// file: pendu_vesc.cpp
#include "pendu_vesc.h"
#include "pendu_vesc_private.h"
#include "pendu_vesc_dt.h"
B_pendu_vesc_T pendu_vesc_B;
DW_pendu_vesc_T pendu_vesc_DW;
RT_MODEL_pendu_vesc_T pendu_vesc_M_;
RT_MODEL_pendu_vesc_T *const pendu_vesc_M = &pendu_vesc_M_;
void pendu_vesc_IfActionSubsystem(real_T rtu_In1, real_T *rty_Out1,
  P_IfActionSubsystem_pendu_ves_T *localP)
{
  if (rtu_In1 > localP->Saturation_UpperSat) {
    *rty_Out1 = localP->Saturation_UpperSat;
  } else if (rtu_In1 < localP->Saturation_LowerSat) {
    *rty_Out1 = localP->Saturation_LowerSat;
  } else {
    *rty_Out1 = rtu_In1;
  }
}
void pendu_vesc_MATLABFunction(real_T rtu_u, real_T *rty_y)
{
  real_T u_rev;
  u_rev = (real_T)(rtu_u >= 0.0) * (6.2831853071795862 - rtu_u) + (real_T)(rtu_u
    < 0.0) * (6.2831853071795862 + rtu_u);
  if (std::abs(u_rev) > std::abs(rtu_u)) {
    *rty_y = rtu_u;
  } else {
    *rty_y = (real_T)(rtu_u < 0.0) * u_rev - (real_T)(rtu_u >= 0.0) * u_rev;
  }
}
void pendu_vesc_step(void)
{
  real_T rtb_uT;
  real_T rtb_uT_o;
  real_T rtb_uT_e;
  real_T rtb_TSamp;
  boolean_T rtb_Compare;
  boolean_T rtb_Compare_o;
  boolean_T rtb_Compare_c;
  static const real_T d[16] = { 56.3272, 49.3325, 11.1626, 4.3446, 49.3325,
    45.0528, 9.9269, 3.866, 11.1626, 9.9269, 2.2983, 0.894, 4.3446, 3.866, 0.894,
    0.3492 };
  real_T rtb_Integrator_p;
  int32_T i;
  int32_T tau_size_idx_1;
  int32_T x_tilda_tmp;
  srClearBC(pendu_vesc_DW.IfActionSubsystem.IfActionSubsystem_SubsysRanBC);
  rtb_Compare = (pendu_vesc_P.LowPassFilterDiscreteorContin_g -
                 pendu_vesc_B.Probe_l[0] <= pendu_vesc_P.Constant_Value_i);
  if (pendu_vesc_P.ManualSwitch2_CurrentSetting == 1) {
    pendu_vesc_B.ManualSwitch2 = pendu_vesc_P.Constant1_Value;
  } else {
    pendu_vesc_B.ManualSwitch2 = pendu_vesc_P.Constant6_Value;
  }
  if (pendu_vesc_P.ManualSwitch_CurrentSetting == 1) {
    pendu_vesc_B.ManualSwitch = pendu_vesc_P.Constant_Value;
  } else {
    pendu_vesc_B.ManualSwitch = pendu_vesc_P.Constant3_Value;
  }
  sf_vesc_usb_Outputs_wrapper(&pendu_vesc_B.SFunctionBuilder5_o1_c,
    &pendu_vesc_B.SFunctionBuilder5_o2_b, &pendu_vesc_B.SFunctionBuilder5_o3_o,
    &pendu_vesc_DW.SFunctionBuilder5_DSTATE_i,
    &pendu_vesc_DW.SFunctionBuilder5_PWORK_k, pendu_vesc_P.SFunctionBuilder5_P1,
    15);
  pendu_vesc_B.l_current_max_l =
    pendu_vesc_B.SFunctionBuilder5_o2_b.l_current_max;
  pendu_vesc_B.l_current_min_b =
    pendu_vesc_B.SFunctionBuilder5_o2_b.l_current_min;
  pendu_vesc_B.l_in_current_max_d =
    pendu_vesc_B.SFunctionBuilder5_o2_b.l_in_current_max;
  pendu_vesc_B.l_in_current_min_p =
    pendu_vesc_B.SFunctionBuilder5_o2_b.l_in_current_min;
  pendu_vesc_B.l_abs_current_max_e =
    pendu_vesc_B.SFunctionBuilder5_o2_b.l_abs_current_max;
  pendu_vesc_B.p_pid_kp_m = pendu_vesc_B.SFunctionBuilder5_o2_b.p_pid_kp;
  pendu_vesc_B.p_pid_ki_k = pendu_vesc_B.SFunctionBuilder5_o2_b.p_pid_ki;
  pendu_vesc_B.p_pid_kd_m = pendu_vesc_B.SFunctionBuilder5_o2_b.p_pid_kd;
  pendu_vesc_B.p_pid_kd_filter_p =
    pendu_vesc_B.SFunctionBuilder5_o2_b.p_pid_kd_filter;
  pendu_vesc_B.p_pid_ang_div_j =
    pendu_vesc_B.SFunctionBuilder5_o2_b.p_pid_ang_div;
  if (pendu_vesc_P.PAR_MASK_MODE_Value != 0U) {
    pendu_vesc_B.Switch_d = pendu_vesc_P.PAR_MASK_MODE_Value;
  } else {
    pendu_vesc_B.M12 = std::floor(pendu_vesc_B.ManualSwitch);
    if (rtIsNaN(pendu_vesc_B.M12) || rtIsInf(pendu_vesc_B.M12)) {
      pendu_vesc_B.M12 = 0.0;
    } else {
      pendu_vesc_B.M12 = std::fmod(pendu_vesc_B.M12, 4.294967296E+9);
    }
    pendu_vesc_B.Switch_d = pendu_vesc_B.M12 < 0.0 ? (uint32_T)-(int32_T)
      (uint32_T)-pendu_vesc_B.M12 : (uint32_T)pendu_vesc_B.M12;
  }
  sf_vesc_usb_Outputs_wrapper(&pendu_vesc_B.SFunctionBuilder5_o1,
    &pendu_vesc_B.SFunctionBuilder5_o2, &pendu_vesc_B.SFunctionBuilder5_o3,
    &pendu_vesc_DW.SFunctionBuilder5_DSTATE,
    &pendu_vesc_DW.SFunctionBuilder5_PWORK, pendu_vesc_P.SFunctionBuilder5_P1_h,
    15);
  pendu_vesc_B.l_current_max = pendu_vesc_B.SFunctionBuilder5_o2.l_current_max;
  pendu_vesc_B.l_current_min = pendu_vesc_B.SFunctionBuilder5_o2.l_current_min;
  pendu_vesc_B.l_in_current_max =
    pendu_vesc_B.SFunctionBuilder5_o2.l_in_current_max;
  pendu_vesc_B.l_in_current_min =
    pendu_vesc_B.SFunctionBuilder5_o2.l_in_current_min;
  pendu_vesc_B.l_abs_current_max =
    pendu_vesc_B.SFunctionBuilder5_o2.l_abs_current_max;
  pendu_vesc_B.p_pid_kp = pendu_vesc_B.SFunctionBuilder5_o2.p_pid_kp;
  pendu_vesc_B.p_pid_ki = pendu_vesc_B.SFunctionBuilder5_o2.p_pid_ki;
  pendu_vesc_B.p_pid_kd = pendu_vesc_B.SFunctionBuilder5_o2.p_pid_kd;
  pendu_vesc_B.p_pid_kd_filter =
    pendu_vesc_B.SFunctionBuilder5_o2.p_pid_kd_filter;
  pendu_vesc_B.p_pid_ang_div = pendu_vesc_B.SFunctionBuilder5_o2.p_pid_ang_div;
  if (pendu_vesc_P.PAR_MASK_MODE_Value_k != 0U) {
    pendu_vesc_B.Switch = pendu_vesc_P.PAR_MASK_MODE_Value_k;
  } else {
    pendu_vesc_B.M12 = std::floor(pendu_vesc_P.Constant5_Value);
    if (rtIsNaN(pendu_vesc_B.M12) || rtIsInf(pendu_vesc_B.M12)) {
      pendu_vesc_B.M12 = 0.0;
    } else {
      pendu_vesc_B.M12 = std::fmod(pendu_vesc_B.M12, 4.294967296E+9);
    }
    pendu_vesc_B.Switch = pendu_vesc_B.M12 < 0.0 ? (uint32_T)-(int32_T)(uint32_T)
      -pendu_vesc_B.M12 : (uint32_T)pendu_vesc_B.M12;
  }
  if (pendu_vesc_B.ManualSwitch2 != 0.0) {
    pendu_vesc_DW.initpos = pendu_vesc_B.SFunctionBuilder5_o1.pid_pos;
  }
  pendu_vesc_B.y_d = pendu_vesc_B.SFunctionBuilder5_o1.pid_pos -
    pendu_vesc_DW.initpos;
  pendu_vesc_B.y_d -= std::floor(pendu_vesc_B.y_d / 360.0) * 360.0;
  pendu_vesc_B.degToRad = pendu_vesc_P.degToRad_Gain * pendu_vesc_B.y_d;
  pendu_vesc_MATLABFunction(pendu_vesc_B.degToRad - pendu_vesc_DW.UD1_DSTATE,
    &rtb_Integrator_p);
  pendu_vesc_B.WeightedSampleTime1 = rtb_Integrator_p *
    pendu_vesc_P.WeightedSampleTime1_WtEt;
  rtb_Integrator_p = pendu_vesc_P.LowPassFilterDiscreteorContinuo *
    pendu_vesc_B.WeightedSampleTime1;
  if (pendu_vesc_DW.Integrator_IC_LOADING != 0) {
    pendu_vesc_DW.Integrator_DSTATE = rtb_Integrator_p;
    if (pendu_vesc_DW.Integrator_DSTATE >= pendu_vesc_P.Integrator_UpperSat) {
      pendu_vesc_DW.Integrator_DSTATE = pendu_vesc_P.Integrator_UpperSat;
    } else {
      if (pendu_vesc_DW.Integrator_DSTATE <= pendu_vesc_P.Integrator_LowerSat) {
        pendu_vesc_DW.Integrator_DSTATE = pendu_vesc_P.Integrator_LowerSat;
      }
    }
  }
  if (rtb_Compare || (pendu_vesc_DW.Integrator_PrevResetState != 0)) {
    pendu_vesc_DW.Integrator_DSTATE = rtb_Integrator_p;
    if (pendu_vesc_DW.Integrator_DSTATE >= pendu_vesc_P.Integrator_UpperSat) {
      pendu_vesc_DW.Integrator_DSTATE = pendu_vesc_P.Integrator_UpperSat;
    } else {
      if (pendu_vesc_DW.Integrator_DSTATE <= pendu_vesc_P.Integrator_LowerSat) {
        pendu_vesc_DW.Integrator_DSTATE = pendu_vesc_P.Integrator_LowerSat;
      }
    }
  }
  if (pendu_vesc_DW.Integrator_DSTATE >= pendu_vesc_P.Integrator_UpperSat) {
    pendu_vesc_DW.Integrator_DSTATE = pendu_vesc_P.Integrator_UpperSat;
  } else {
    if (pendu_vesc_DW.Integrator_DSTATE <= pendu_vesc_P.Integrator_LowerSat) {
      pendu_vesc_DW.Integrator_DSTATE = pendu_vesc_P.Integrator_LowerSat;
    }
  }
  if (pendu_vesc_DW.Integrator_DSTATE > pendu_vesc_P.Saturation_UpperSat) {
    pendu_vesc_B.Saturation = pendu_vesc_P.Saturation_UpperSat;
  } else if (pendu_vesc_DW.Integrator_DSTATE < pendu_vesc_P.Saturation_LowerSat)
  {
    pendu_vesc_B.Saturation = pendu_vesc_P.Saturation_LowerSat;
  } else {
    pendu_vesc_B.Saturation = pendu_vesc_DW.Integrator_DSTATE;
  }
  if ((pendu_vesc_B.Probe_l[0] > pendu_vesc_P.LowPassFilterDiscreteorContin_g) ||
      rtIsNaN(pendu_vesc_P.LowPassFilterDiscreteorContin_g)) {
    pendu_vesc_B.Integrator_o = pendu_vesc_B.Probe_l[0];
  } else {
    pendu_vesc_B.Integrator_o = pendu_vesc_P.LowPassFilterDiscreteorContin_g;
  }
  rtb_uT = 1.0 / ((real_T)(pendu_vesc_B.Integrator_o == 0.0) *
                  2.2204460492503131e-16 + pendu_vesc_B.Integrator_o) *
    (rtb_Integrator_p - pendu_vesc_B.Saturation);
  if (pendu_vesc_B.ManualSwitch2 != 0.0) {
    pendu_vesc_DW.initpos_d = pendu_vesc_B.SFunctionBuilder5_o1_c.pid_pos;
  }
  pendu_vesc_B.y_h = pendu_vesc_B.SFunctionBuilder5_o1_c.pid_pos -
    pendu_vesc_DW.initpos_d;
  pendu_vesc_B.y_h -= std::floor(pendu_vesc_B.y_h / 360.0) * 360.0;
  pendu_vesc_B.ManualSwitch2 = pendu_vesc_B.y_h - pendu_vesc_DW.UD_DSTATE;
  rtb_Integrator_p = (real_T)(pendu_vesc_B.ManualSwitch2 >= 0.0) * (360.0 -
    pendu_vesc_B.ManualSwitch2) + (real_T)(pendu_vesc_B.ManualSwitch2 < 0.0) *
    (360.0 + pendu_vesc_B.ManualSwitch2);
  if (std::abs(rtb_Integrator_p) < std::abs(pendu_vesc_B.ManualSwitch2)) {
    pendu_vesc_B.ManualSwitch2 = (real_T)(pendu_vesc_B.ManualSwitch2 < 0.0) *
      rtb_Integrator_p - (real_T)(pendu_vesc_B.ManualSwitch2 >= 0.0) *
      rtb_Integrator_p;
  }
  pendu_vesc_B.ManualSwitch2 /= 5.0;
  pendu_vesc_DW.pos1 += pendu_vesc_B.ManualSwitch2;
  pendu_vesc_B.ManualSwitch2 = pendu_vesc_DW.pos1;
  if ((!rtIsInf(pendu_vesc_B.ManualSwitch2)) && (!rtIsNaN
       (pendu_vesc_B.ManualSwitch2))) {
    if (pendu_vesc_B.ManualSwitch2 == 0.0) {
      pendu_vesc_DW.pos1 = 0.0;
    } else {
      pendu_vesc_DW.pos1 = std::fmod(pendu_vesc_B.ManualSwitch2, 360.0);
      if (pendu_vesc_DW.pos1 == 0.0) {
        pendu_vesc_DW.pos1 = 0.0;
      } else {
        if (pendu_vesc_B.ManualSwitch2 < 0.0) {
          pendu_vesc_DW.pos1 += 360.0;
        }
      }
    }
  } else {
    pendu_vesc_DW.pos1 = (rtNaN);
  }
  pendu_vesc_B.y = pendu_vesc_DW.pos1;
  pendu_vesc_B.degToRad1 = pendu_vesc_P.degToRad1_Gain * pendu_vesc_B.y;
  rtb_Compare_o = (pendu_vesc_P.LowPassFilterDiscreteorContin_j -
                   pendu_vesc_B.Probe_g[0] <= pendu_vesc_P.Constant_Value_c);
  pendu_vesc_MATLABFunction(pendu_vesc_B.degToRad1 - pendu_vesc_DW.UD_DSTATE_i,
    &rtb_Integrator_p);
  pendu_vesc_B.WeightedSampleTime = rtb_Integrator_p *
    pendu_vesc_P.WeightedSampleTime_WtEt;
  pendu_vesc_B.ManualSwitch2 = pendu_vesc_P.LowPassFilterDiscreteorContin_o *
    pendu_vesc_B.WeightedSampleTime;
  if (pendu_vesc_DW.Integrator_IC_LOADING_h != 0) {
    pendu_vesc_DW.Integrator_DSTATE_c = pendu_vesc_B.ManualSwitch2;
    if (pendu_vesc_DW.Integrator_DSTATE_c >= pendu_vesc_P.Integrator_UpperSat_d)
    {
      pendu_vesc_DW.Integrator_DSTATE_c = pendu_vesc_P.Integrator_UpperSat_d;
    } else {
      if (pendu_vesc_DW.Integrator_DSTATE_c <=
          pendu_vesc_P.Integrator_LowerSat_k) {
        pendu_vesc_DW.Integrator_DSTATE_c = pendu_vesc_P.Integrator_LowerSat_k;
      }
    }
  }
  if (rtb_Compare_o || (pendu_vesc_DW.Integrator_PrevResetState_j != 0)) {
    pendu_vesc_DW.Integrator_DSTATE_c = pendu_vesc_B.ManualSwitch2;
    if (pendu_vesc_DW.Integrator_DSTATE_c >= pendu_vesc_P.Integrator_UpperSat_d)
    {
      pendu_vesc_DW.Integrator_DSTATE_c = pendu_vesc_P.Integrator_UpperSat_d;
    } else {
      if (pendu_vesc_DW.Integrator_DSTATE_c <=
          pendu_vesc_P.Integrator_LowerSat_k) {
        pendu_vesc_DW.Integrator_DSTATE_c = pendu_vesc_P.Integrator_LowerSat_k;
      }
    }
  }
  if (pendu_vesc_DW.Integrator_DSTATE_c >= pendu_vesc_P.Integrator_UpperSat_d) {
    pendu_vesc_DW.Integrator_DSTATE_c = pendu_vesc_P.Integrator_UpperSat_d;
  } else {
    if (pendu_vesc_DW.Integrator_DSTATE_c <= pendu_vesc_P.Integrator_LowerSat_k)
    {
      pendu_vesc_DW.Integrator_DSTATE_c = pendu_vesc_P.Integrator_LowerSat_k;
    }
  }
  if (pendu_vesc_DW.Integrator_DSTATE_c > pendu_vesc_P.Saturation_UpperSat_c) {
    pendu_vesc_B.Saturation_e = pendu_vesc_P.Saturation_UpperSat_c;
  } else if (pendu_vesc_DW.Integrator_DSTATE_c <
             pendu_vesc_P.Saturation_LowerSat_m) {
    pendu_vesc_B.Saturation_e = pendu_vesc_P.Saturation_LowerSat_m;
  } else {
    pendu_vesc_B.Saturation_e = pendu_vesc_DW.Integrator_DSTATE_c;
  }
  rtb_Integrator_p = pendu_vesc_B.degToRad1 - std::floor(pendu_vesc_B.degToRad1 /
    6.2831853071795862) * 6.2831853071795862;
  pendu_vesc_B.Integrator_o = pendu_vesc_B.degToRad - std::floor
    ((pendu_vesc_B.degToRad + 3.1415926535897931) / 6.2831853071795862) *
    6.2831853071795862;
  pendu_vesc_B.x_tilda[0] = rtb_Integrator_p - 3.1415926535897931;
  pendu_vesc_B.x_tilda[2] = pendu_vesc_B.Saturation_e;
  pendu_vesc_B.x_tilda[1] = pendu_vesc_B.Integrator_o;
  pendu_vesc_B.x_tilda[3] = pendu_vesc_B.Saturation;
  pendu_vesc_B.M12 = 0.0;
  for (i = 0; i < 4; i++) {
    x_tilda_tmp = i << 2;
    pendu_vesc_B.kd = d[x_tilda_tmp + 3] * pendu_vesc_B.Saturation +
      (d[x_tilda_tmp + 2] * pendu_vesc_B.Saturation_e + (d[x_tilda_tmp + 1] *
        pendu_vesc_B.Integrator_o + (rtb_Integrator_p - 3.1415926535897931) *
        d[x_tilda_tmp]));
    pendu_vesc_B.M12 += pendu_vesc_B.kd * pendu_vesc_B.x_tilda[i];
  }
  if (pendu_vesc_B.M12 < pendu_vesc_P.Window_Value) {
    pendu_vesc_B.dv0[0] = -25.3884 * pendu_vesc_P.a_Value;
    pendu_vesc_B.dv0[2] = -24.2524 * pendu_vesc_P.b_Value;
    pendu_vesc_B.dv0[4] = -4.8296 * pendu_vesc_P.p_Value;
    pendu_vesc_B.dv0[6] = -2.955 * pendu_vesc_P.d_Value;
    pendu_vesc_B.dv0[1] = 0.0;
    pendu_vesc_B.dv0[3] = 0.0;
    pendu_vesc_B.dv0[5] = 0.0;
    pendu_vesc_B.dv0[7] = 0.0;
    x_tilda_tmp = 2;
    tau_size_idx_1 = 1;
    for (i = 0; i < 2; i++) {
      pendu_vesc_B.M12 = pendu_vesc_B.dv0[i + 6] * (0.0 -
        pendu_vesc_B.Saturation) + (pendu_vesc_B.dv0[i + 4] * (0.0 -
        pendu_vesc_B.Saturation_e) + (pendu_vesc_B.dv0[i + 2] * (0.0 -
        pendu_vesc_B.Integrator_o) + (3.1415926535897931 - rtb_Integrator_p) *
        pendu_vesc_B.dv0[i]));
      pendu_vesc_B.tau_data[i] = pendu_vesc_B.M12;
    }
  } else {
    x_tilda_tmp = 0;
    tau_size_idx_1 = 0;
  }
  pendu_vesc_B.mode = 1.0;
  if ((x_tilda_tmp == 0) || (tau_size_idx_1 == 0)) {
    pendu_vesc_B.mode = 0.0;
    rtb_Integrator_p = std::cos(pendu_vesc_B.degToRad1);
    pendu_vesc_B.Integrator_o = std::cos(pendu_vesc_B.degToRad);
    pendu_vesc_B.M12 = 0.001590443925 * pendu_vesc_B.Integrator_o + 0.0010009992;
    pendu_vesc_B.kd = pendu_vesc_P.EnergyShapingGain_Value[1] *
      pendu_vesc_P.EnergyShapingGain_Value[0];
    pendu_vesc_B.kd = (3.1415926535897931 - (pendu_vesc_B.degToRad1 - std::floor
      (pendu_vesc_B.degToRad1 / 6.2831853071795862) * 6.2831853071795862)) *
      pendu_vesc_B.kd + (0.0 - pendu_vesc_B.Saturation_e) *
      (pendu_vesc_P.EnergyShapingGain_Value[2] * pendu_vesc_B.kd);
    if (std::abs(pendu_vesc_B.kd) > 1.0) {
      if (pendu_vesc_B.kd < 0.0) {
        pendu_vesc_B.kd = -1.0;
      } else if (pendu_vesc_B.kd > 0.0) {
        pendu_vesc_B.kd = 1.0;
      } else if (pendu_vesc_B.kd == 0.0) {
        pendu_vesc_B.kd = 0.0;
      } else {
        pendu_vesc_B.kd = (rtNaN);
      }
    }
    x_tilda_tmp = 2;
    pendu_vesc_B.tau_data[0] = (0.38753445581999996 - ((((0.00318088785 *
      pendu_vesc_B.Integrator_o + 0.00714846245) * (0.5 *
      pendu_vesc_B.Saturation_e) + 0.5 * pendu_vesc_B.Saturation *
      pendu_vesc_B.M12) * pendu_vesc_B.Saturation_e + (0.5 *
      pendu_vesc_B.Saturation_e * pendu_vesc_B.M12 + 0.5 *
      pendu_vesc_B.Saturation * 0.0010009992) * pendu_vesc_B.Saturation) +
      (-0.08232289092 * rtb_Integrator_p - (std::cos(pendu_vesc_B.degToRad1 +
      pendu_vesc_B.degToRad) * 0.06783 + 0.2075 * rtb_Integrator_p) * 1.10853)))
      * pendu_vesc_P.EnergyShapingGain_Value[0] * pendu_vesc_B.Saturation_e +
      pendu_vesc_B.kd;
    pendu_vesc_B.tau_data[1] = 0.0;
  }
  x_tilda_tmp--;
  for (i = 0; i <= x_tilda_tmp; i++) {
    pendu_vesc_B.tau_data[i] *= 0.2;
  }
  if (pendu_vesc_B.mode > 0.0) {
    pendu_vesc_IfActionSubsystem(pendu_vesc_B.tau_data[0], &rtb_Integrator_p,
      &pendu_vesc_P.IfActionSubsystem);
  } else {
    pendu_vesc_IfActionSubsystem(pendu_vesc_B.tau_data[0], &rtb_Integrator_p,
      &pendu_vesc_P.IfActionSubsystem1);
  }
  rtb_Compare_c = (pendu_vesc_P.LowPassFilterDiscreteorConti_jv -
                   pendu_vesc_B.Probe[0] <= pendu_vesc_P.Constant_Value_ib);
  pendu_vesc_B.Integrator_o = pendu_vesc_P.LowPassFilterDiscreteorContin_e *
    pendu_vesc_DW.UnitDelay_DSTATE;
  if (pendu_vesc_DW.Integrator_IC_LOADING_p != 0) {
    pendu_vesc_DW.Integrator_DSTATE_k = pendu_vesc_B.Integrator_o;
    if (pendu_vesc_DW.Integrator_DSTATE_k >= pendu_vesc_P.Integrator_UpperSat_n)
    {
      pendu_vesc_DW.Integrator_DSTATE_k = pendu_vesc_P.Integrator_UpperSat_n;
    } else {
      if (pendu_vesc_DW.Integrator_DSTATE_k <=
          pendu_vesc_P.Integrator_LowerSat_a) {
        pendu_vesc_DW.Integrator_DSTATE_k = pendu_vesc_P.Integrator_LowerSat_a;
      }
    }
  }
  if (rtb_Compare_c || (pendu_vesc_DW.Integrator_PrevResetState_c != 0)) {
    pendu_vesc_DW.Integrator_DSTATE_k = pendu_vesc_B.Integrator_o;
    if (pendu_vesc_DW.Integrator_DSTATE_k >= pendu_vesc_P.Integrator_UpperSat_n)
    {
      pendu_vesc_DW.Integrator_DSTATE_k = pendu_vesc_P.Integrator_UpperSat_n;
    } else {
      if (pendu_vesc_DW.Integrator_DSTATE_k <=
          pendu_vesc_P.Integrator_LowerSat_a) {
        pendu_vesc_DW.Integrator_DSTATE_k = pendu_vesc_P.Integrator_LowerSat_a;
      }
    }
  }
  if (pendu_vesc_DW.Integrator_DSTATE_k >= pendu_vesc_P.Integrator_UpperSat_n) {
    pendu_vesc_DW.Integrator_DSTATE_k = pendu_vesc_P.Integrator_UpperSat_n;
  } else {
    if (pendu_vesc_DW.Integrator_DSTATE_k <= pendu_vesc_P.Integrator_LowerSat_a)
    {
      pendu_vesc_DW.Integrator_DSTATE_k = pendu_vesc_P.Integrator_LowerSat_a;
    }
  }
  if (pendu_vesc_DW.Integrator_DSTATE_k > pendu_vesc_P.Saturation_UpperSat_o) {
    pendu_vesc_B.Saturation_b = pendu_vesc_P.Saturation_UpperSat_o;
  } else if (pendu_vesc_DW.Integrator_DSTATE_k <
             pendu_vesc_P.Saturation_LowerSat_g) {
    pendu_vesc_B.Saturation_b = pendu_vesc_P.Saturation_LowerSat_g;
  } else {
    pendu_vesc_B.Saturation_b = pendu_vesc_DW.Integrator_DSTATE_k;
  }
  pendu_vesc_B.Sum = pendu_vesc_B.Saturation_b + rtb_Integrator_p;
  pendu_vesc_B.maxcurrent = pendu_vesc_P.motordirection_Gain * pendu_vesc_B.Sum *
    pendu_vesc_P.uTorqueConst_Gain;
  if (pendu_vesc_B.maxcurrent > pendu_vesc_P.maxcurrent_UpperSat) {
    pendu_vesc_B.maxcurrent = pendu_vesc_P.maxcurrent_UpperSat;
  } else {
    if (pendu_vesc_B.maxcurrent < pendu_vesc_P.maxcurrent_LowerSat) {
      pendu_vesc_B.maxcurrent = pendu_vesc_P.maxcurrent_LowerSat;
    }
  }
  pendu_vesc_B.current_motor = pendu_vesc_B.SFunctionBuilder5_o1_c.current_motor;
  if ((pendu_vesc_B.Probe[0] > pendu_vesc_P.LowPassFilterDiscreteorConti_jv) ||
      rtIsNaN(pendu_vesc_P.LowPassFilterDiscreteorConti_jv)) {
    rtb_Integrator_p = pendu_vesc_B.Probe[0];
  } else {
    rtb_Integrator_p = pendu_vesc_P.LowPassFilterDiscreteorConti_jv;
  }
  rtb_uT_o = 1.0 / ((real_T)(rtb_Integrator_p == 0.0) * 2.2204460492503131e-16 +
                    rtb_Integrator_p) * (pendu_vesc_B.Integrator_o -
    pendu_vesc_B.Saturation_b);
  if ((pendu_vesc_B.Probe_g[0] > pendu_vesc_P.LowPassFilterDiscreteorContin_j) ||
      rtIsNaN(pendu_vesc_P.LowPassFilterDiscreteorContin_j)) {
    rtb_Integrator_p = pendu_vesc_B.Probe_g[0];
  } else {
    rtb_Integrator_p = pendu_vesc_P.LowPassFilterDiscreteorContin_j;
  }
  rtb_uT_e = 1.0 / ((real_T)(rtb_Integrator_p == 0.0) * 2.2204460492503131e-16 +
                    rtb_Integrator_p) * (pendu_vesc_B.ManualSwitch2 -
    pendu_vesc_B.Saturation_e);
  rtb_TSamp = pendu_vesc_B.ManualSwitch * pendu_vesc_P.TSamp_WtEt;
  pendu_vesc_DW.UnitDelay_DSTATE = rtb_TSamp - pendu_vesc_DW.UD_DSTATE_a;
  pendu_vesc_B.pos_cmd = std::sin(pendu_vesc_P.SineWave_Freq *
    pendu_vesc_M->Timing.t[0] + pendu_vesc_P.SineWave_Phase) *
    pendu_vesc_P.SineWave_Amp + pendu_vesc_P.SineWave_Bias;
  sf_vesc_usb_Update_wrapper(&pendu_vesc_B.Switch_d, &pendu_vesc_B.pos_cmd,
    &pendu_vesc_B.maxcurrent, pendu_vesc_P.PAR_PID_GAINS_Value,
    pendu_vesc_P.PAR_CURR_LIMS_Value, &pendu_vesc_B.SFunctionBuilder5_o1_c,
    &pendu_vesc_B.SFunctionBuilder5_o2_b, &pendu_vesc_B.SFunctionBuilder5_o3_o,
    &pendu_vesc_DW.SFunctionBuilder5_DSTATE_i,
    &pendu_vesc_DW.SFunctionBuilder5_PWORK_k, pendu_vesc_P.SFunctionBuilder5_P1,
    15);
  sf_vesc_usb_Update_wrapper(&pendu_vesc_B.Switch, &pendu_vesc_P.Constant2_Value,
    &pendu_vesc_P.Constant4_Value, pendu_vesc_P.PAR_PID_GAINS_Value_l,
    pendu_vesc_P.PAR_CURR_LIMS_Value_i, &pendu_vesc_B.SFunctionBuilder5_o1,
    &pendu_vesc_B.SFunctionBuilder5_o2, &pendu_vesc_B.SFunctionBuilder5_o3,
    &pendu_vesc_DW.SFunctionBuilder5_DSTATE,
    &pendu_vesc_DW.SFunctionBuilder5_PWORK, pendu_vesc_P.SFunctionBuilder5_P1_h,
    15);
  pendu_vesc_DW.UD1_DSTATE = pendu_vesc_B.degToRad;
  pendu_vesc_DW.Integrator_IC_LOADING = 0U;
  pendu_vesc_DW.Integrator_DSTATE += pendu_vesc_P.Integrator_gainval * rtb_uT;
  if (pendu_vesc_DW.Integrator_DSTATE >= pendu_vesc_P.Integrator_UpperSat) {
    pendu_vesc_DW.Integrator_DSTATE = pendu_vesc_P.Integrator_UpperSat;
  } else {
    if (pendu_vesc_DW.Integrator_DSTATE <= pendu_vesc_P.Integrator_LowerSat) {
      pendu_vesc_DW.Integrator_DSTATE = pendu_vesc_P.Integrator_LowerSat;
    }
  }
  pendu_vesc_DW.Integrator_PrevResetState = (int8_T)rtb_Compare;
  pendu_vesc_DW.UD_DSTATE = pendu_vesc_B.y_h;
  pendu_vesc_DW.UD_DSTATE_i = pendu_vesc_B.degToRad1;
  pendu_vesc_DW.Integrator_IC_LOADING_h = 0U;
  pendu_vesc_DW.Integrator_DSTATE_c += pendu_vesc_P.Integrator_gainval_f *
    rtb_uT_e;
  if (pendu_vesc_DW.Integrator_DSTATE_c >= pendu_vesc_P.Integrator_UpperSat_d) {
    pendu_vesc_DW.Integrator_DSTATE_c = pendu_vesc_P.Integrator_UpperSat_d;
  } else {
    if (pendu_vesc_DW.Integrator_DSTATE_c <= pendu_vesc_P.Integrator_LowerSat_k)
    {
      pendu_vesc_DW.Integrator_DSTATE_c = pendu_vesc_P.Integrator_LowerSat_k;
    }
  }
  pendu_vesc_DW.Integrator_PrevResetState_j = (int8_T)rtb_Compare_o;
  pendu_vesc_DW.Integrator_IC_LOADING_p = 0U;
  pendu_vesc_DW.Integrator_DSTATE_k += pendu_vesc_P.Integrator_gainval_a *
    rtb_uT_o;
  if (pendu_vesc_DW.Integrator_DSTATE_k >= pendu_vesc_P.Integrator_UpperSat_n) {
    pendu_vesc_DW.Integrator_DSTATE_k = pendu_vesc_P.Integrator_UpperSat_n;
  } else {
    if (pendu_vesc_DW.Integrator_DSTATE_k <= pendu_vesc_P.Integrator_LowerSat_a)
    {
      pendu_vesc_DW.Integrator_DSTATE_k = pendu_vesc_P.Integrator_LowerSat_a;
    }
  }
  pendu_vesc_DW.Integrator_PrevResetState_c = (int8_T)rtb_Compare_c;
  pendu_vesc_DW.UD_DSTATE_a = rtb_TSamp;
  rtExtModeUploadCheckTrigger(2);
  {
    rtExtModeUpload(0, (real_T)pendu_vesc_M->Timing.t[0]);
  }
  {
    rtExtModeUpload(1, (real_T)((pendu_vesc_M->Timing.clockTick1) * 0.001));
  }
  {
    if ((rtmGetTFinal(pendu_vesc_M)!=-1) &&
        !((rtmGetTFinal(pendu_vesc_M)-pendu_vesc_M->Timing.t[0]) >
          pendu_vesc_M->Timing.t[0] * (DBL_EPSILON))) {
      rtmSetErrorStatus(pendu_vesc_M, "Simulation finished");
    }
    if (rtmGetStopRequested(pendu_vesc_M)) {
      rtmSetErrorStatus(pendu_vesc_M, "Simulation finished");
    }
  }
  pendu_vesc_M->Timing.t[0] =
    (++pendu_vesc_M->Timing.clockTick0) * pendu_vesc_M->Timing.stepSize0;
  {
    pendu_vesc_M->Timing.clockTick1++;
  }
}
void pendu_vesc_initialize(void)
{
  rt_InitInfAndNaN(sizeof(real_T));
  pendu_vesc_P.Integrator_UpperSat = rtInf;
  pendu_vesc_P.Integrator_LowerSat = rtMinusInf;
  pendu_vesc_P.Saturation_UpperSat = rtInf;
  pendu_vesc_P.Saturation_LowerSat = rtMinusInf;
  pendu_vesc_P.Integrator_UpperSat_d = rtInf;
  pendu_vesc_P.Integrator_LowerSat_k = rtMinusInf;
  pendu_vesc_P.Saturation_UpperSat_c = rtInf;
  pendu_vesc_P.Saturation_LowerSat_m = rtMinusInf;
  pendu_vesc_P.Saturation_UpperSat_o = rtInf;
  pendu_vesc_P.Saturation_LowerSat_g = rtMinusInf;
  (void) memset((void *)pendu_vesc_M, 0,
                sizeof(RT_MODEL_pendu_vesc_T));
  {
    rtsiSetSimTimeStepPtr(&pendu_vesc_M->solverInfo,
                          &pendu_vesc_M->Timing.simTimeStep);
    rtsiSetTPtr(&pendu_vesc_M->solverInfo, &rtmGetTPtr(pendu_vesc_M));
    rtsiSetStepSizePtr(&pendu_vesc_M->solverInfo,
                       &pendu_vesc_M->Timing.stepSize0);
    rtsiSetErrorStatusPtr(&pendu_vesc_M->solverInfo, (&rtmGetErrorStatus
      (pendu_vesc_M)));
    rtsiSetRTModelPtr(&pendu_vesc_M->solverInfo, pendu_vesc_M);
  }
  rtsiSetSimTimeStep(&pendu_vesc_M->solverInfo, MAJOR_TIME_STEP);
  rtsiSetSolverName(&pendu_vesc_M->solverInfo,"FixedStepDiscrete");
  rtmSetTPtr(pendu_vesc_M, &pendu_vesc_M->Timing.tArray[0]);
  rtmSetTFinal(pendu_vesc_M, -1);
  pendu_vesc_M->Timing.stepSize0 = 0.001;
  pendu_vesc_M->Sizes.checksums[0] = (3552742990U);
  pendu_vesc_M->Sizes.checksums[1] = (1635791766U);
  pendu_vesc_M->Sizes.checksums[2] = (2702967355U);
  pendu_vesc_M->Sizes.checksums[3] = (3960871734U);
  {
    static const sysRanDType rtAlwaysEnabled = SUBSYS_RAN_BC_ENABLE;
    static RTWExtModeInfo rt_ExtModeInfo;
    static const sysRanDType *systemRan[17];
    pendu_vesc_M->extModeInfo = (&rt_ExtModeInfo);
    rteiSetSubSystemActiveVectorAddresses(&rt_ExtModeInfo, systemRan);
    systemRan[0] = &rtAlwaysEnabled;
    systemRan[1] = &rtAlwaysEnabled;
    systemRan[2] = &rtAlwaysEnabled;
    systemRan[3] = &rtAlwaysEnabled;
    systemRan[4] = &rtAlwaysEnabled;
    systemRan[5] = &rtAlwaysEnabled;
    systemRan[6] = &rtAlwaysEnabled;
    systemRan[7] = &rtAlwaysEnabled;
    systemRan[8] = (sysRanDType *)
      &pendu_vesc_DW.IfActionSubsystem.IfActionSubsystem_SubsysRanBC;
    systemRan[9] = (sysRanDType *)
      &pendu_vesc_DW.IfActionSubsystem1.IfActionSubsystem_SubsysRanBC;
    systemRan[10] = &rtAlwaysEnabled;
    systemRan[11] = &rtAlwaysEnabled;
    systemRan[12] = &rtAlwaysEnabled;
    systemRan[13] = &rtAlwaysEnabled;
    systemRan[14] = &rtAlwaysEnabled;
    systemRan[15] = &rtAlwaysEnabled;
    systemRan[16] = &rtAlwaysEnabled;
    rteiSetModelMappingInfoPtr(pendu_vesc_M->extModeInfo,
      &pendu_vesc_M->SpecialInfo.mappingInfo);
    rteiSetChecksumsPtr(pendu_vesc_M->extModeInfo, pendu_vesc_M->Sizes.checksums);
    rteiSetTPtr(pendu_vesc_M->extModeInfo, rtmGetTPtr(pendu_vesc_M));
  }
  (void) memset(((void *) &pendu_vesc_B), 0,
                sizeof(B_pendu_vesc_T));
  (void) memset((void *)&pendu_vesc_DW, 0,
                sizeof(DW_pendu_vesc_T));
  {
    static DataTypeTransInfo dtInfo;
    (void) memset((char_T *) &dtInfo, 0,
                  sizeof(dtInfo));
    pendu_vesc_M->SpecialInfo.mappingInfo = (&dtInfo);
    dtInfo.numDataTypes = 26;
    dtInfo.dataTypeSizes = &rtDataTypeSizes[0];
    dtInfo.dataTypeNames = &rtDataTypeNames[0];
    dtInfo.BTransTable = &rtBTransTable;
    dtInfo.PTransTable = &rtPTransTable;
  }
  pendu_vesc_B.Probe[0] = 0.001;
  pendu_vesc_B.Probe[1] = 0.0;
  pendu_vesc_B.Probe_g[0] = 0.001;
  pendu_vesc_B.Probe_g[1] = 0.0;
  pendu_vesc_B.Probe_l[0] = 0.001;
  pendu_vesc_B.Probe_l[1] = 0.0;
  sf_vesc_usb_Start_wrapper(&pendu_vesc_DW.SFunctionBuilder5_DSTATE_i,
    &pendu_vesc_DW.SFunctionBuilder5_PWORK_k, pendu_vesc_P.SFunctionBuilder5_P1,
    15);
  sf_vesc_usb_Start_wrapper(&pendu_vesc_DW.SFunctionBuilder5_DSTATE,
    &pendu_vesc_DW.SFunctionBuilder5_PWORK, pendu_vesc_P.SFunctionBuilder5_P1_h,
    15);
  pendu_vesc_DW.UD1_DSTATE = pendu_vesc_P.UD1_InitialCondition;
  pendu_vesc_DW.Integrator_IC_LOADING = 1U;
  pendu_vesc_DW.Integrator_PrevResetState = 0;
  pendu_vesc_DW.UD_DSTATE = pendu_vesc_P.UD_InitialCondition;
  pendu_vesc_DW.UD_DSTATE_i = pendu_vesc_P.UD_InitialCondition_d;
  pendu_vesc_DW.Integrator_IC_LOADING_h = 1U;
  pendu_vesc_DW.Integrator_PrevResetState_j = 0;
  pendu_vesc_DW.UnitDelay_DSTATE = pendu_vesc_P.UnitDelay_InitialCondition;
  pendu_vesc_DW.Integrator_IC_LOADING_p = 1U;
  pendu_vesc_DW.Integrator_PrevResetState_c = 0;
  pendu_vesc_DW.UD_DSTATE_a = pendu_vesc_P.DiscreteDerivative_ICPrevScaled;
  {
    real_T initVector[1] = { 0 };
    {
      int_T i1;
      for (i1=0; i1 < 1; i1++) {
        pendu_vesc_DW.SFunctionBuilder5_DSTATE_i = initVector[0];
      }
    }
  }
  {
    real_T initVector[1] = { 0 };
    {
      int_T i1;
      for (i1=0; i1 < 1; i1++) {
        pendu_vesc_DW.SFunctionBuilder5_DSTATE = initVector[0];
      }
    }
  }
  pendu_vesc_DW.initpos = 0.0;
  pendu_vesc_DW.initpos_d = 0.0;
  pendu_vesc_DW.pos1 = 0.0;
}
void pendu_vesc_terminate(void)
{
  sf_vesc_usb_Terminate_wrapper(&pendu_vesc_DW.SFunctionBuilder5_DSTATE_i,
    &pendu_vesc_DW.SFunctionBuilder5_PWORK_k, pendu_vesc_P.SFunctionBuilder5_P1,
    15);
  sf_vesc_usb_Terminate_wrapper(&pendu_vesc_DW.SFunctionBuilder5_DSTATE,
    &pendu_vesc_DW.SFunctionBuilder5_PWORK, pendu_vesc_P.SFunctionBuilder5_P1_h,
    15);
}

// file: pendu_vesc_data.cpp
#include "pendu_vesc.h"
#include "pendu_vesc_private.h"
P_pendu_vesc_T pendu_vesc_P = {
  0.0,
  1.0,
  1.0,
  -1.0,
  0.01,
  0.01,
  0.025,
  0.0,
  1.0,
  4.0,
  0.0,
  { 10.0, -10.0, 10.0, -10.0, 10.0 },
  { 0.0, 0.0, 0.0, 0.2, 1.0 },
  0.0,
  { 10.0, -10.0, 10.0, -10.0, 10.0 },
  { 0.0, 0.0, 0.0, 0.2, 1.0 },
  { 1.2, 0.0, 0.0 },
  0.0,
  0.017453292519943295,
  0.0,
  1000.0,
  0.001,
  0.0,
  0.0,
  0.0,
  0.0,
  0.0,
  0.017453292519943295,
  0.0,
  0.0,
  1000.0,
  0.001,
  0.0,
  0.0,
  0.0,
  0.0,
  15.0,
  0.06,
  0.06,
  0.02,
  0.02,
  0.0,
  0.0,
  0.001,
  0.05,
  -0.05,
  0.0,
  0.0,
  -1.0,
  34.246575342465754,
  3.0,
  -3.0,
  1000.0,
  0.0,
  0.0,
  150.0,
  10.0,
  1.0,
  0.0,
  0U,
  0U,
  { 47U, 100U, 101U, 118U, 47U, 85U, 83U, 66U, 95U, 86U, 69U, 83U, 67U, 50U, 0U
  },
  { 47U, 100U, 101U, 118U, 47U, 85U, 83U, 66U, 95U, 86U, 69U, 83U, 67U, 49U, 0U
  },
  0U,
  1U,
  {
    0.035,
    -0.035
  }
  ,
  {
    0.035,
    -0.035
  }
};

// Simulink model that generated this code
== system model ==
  DataTypeDuplicate#1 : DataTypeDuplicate  <- 1: WeightedSampleTime1, 2: degToRad, 3: UD1
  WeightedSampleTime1 : SampleTimeMath  <- 1: MATLABFunction#1
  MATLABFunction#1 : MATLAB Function  <- 1: Sum#1
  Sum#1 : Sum  Inputs=+-  <- 1: degToRad, 2: UD1
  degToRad : Gain  Gain=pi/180  <- 1: DataTypeConversion#1
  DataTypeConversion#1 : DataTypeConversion  <- 1: MATLABFunction#2
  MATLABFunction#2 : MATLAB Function  <- 1: ManualSwitch2, 2: DataTypeConversion#2
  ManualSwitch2 : ManualSwitch  <- 1: Constant1, 2: Constant6
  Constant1 : Constant
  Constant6 : Constant  Value=0
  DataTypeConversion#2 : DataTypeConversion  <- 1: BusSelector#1
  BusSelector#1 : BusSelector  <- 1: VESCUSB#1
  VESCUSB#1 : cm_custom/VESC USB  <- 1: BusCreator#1
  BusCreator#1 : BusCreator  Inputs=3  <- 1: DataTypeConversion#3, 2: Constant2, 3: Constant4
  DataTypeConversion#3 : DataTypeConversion  <- 1: Constant5
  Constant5 : Constant  Value=0
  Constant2 : Constant  Value=0
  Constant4 : Constant  Value=0
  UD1 : UnitDelay  <- 1: degToRad
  DataTypeDuplicate#2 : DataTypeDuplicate  <- 1: MATLABFunction, 2: MATLABFunction#3, 3: UD
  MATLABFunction : MATLAB Function  <- 1: Sum#2
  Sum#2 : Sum  Inputs=+-  <- 1: MATLABFunction#3, 2: UD
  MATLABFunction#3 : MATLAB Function  <- 1: ManualSwitch2, 2: DataTypeConversion#4
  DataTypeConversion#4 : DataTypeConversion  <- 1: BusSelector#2
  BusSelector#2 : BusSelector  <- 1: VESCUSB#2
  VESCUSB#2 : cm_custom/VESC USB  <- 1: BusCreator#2
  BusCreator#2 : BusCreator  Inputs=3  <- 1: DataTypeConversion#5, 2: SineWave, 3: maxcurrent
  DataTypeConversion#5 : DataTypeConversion  <- 1: ManualSwitch
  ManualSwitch : ManualSwitch  <- 1: Constant, 2: Constant3
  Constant : Constant  Value=0
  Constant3 : Constant  Value=4
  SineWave : Sin  Amplitude=150  Bias=10
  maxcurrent : Saturate  UpperLimit=3  LowerLimit=-3  <- 1: Gain#1
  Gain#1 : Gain  Gain=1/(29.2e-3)  <- 1: motordirection
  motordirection : Gain  Gain=-1  <- 1: Sum
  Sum : Sum  <- 1: LowPassFilterDiscreteorContinuous#1, 2: Merge#1
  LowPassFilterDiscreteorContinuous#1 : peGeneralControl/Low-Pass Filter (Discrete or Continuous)  B=0.05  A=-0.05  <- 1: UnitDelay
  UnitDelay : UnitDelay  <- 1: DiscreteDerivative
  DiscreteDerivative : simulink/Discrete/Discrete Derivative  gainval=1.0  <- 1: ManualSwitch
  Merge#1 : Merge  <- 1: IfActionSubsystem, 2: IfActionSubsystem1
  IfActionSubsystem : Subsystem  <- 1: MATLABFunction#4, Action: If#1
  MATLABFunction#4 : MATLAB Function  <- 1: degToRad1, 2: degToRad, 3: LowPassFilterDiscreteorContinuous#2, 4: LowPassFilterDiscreteorContinuous#3, 5: EnergyShapingGain, 6: Window, 7: Constant#1, 8: Constant#2, 9: Constant#3, 10: Constant#4
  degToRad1 : Gain  Gain=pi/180  <- 1: DataTypeConversion#6
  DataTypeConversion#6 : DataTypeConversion  <- 1: MATLABFunction
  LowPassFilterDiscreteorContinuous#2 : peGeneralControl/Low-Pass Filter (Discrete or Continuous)  B=inf  A=-inf  <- 1: WeightedSampleTime
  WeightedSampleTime : SampleTimeMath  <- 1: MATLABFunction#5
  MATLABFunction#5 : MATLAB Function  <- 1: Sum#3
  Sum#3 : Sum  Inputs=+-  <- 1: degToRad1, 2: UnitDelay#1
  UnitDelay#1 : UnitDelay  <- 1: degToRad1
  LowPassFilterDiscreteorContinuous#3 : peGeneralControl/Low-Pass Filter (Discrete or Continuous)  B=inf  A=-inf  <- 1: WeightedSampleTime1
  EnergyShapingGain : Constant  Value=[1.2 0 0]
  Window : Constant  Value=15
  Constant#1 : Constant  Value=0.06
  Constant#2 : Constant  Value=0.06
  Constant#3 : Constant  Value=0.02
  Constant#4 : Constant  Value=0.02
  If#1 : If  <- 1: MATLABFunction#4/3
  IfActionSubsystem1 : Subsystem  <- 1: MATLABFunction#4, Action: If#1/2
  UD : UnitDelay  <- 1: MATLABFunction#3
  DataTypeDuplicate#3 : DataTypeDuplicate  <- 1: WeightedSampleTime, 2: degToRad1, 3: UnitDelay#1
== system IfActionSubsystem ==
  In1 : Inport
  ActionPort#1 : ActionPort
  Out1 : Outport  <- 1: Saturation
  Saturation : Saturate  UpperLimit=0.035  LowerLimit=-0.035  <- 1: In1
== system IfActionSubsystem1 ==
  Inport#1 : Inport
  ActionPort#2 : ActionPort
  Outport#1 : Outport  <- 1: Saturate#1
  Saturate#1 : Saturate  UpperLimit=0.035  LowerLimit=-0.035  <- 1: Inport#1
== matlab function MATLAB Function ==
function y = fcn(setzero,u)

persistent initpos
if isempty(initpos)
    initpos = 0;
end

if setzero
    initpos = u + 0;
end

y = u - initpos;
y = y - 360*floor(y/360);

== matlab function MATLABFunction#4 ==
function [tau1,tau2,mode] = EnergyShaping_w_LQR(x1,x2,dx1,dx2,K,wdw,a,b,p,d)
% Match the setup in simulation
x = [x1;x2;dx1;dx2]; 

persistent model;
if isempty(model)
    model = Model();
end

%%%%
q  = x(1:2,:);
qd = x(3:4,:);

[tau,mode] = acrobotControlLaw_LQR(x,wdw,a,b,p,d);

if isempty(tau) % if LQR control law is not applicable, 
                %    then using Energy Shaping approach
    mode = 0;
    g  = model.g;
    %
    l1 = model.l1; lc1 = model.lc1; l2 = model.l2; lc2 = model.lc2;
    m1 = model.m1; m2 = model.m2;
    I1 = model.I1; I2 = model.I2;
    b1 = model.b1; b2 = model.b2;

    %%%%
    q  = x(1:2,:);
    qd = x(3:4,:);

    %%%%
    c = cos(q(1:2,:));  s = sin(q(1:2,:));  c12 = cos(q(1,:)+q(2,:));
    
    [M,~] = ManipulatorEquation(model, x);
    %%%% energy shaping
    E_des = m1.*g.* lc1 + m2.*g.*(l1+lc2);

    KE = 0.5*qd.'*M*qd;
    PE = -m1*g*lc1*c(1) - m2*g*(l1*c(1)+lc2*c12);
    E = KE + PE;

    E_tilda = E_des - E;

%     ke = 1;    %0.75  %5   %0.05;
%     kd = 0*ke/10;  %25   %ke/15;
%     ks = 0*kd/5;   %8   %kd/10;
    ke = K(1);
    kd = K(2)*ke;
    ks = K(3)*kd;
    
    q(1) = q(1) - 2*pi*floor(q(1)./(2*pi));
    d_tilda = pi-q(1);
    s_tilda = 0-qd(1);
    
    % P-saturation
    PD = d_tilda*kd + s_tilda*ks;
    if abs(PD) > 1
        PD = 1 * sign(PD);
    end
    
    tau = [(ke.*E_tilda.*qd(1)+PD); 0]; 
%     tau = [(0); 0]; 
    
end
tau=(18/90)*tau;
tau1 = tau(1);

tau2 = tau(2);
end

== matlab function MATLAB Function1 ==
function y = fcn(setzero,u)

persistent initpos
if isempty(initpos)
    initpos = 0;
end

if setzero
    initpos = u + 0;
end

y = u - initpos;
y = y - 360*floor(y/360);

== matlab function MATLAB Function ==
function y = fcn(u)

u_rev = (u >= 0)*(2*pi - u) + (u < 0)*(2*pi + u);

if abs(u_rev) > abs(u)
   y = u;
else
   y = (u < 0)*u_rev - (u >= 0)*u_rev;
end

== matlab function MATLAB Function1 ==
function y = fcn(u)

u_rev = (u >= 0)*(2*pi - u) + (u < 0)*(2*pi + u);

if abs(u_rev) > abs(u)
   y = u;
else
   y = (u < 0)*u_rev - (u >= 0)*u_rev;
end

== matlab function MATLAB Function ==
function y = fcn(u)

persistent pos1
if isempty(pos1)
    pos1 = 0;
end

u_rev = (u >= 0)*(360 - u) + (u < 0)*(360 + u);
if abs(u_rev) < abs(u)
   u = (u < 0)*u_rev - (u >= 0)*u_rev;
end

u = u/5;
pos1 = pos1 + u;
pos1 = mod((pos1),360);
y = pos1;

end
